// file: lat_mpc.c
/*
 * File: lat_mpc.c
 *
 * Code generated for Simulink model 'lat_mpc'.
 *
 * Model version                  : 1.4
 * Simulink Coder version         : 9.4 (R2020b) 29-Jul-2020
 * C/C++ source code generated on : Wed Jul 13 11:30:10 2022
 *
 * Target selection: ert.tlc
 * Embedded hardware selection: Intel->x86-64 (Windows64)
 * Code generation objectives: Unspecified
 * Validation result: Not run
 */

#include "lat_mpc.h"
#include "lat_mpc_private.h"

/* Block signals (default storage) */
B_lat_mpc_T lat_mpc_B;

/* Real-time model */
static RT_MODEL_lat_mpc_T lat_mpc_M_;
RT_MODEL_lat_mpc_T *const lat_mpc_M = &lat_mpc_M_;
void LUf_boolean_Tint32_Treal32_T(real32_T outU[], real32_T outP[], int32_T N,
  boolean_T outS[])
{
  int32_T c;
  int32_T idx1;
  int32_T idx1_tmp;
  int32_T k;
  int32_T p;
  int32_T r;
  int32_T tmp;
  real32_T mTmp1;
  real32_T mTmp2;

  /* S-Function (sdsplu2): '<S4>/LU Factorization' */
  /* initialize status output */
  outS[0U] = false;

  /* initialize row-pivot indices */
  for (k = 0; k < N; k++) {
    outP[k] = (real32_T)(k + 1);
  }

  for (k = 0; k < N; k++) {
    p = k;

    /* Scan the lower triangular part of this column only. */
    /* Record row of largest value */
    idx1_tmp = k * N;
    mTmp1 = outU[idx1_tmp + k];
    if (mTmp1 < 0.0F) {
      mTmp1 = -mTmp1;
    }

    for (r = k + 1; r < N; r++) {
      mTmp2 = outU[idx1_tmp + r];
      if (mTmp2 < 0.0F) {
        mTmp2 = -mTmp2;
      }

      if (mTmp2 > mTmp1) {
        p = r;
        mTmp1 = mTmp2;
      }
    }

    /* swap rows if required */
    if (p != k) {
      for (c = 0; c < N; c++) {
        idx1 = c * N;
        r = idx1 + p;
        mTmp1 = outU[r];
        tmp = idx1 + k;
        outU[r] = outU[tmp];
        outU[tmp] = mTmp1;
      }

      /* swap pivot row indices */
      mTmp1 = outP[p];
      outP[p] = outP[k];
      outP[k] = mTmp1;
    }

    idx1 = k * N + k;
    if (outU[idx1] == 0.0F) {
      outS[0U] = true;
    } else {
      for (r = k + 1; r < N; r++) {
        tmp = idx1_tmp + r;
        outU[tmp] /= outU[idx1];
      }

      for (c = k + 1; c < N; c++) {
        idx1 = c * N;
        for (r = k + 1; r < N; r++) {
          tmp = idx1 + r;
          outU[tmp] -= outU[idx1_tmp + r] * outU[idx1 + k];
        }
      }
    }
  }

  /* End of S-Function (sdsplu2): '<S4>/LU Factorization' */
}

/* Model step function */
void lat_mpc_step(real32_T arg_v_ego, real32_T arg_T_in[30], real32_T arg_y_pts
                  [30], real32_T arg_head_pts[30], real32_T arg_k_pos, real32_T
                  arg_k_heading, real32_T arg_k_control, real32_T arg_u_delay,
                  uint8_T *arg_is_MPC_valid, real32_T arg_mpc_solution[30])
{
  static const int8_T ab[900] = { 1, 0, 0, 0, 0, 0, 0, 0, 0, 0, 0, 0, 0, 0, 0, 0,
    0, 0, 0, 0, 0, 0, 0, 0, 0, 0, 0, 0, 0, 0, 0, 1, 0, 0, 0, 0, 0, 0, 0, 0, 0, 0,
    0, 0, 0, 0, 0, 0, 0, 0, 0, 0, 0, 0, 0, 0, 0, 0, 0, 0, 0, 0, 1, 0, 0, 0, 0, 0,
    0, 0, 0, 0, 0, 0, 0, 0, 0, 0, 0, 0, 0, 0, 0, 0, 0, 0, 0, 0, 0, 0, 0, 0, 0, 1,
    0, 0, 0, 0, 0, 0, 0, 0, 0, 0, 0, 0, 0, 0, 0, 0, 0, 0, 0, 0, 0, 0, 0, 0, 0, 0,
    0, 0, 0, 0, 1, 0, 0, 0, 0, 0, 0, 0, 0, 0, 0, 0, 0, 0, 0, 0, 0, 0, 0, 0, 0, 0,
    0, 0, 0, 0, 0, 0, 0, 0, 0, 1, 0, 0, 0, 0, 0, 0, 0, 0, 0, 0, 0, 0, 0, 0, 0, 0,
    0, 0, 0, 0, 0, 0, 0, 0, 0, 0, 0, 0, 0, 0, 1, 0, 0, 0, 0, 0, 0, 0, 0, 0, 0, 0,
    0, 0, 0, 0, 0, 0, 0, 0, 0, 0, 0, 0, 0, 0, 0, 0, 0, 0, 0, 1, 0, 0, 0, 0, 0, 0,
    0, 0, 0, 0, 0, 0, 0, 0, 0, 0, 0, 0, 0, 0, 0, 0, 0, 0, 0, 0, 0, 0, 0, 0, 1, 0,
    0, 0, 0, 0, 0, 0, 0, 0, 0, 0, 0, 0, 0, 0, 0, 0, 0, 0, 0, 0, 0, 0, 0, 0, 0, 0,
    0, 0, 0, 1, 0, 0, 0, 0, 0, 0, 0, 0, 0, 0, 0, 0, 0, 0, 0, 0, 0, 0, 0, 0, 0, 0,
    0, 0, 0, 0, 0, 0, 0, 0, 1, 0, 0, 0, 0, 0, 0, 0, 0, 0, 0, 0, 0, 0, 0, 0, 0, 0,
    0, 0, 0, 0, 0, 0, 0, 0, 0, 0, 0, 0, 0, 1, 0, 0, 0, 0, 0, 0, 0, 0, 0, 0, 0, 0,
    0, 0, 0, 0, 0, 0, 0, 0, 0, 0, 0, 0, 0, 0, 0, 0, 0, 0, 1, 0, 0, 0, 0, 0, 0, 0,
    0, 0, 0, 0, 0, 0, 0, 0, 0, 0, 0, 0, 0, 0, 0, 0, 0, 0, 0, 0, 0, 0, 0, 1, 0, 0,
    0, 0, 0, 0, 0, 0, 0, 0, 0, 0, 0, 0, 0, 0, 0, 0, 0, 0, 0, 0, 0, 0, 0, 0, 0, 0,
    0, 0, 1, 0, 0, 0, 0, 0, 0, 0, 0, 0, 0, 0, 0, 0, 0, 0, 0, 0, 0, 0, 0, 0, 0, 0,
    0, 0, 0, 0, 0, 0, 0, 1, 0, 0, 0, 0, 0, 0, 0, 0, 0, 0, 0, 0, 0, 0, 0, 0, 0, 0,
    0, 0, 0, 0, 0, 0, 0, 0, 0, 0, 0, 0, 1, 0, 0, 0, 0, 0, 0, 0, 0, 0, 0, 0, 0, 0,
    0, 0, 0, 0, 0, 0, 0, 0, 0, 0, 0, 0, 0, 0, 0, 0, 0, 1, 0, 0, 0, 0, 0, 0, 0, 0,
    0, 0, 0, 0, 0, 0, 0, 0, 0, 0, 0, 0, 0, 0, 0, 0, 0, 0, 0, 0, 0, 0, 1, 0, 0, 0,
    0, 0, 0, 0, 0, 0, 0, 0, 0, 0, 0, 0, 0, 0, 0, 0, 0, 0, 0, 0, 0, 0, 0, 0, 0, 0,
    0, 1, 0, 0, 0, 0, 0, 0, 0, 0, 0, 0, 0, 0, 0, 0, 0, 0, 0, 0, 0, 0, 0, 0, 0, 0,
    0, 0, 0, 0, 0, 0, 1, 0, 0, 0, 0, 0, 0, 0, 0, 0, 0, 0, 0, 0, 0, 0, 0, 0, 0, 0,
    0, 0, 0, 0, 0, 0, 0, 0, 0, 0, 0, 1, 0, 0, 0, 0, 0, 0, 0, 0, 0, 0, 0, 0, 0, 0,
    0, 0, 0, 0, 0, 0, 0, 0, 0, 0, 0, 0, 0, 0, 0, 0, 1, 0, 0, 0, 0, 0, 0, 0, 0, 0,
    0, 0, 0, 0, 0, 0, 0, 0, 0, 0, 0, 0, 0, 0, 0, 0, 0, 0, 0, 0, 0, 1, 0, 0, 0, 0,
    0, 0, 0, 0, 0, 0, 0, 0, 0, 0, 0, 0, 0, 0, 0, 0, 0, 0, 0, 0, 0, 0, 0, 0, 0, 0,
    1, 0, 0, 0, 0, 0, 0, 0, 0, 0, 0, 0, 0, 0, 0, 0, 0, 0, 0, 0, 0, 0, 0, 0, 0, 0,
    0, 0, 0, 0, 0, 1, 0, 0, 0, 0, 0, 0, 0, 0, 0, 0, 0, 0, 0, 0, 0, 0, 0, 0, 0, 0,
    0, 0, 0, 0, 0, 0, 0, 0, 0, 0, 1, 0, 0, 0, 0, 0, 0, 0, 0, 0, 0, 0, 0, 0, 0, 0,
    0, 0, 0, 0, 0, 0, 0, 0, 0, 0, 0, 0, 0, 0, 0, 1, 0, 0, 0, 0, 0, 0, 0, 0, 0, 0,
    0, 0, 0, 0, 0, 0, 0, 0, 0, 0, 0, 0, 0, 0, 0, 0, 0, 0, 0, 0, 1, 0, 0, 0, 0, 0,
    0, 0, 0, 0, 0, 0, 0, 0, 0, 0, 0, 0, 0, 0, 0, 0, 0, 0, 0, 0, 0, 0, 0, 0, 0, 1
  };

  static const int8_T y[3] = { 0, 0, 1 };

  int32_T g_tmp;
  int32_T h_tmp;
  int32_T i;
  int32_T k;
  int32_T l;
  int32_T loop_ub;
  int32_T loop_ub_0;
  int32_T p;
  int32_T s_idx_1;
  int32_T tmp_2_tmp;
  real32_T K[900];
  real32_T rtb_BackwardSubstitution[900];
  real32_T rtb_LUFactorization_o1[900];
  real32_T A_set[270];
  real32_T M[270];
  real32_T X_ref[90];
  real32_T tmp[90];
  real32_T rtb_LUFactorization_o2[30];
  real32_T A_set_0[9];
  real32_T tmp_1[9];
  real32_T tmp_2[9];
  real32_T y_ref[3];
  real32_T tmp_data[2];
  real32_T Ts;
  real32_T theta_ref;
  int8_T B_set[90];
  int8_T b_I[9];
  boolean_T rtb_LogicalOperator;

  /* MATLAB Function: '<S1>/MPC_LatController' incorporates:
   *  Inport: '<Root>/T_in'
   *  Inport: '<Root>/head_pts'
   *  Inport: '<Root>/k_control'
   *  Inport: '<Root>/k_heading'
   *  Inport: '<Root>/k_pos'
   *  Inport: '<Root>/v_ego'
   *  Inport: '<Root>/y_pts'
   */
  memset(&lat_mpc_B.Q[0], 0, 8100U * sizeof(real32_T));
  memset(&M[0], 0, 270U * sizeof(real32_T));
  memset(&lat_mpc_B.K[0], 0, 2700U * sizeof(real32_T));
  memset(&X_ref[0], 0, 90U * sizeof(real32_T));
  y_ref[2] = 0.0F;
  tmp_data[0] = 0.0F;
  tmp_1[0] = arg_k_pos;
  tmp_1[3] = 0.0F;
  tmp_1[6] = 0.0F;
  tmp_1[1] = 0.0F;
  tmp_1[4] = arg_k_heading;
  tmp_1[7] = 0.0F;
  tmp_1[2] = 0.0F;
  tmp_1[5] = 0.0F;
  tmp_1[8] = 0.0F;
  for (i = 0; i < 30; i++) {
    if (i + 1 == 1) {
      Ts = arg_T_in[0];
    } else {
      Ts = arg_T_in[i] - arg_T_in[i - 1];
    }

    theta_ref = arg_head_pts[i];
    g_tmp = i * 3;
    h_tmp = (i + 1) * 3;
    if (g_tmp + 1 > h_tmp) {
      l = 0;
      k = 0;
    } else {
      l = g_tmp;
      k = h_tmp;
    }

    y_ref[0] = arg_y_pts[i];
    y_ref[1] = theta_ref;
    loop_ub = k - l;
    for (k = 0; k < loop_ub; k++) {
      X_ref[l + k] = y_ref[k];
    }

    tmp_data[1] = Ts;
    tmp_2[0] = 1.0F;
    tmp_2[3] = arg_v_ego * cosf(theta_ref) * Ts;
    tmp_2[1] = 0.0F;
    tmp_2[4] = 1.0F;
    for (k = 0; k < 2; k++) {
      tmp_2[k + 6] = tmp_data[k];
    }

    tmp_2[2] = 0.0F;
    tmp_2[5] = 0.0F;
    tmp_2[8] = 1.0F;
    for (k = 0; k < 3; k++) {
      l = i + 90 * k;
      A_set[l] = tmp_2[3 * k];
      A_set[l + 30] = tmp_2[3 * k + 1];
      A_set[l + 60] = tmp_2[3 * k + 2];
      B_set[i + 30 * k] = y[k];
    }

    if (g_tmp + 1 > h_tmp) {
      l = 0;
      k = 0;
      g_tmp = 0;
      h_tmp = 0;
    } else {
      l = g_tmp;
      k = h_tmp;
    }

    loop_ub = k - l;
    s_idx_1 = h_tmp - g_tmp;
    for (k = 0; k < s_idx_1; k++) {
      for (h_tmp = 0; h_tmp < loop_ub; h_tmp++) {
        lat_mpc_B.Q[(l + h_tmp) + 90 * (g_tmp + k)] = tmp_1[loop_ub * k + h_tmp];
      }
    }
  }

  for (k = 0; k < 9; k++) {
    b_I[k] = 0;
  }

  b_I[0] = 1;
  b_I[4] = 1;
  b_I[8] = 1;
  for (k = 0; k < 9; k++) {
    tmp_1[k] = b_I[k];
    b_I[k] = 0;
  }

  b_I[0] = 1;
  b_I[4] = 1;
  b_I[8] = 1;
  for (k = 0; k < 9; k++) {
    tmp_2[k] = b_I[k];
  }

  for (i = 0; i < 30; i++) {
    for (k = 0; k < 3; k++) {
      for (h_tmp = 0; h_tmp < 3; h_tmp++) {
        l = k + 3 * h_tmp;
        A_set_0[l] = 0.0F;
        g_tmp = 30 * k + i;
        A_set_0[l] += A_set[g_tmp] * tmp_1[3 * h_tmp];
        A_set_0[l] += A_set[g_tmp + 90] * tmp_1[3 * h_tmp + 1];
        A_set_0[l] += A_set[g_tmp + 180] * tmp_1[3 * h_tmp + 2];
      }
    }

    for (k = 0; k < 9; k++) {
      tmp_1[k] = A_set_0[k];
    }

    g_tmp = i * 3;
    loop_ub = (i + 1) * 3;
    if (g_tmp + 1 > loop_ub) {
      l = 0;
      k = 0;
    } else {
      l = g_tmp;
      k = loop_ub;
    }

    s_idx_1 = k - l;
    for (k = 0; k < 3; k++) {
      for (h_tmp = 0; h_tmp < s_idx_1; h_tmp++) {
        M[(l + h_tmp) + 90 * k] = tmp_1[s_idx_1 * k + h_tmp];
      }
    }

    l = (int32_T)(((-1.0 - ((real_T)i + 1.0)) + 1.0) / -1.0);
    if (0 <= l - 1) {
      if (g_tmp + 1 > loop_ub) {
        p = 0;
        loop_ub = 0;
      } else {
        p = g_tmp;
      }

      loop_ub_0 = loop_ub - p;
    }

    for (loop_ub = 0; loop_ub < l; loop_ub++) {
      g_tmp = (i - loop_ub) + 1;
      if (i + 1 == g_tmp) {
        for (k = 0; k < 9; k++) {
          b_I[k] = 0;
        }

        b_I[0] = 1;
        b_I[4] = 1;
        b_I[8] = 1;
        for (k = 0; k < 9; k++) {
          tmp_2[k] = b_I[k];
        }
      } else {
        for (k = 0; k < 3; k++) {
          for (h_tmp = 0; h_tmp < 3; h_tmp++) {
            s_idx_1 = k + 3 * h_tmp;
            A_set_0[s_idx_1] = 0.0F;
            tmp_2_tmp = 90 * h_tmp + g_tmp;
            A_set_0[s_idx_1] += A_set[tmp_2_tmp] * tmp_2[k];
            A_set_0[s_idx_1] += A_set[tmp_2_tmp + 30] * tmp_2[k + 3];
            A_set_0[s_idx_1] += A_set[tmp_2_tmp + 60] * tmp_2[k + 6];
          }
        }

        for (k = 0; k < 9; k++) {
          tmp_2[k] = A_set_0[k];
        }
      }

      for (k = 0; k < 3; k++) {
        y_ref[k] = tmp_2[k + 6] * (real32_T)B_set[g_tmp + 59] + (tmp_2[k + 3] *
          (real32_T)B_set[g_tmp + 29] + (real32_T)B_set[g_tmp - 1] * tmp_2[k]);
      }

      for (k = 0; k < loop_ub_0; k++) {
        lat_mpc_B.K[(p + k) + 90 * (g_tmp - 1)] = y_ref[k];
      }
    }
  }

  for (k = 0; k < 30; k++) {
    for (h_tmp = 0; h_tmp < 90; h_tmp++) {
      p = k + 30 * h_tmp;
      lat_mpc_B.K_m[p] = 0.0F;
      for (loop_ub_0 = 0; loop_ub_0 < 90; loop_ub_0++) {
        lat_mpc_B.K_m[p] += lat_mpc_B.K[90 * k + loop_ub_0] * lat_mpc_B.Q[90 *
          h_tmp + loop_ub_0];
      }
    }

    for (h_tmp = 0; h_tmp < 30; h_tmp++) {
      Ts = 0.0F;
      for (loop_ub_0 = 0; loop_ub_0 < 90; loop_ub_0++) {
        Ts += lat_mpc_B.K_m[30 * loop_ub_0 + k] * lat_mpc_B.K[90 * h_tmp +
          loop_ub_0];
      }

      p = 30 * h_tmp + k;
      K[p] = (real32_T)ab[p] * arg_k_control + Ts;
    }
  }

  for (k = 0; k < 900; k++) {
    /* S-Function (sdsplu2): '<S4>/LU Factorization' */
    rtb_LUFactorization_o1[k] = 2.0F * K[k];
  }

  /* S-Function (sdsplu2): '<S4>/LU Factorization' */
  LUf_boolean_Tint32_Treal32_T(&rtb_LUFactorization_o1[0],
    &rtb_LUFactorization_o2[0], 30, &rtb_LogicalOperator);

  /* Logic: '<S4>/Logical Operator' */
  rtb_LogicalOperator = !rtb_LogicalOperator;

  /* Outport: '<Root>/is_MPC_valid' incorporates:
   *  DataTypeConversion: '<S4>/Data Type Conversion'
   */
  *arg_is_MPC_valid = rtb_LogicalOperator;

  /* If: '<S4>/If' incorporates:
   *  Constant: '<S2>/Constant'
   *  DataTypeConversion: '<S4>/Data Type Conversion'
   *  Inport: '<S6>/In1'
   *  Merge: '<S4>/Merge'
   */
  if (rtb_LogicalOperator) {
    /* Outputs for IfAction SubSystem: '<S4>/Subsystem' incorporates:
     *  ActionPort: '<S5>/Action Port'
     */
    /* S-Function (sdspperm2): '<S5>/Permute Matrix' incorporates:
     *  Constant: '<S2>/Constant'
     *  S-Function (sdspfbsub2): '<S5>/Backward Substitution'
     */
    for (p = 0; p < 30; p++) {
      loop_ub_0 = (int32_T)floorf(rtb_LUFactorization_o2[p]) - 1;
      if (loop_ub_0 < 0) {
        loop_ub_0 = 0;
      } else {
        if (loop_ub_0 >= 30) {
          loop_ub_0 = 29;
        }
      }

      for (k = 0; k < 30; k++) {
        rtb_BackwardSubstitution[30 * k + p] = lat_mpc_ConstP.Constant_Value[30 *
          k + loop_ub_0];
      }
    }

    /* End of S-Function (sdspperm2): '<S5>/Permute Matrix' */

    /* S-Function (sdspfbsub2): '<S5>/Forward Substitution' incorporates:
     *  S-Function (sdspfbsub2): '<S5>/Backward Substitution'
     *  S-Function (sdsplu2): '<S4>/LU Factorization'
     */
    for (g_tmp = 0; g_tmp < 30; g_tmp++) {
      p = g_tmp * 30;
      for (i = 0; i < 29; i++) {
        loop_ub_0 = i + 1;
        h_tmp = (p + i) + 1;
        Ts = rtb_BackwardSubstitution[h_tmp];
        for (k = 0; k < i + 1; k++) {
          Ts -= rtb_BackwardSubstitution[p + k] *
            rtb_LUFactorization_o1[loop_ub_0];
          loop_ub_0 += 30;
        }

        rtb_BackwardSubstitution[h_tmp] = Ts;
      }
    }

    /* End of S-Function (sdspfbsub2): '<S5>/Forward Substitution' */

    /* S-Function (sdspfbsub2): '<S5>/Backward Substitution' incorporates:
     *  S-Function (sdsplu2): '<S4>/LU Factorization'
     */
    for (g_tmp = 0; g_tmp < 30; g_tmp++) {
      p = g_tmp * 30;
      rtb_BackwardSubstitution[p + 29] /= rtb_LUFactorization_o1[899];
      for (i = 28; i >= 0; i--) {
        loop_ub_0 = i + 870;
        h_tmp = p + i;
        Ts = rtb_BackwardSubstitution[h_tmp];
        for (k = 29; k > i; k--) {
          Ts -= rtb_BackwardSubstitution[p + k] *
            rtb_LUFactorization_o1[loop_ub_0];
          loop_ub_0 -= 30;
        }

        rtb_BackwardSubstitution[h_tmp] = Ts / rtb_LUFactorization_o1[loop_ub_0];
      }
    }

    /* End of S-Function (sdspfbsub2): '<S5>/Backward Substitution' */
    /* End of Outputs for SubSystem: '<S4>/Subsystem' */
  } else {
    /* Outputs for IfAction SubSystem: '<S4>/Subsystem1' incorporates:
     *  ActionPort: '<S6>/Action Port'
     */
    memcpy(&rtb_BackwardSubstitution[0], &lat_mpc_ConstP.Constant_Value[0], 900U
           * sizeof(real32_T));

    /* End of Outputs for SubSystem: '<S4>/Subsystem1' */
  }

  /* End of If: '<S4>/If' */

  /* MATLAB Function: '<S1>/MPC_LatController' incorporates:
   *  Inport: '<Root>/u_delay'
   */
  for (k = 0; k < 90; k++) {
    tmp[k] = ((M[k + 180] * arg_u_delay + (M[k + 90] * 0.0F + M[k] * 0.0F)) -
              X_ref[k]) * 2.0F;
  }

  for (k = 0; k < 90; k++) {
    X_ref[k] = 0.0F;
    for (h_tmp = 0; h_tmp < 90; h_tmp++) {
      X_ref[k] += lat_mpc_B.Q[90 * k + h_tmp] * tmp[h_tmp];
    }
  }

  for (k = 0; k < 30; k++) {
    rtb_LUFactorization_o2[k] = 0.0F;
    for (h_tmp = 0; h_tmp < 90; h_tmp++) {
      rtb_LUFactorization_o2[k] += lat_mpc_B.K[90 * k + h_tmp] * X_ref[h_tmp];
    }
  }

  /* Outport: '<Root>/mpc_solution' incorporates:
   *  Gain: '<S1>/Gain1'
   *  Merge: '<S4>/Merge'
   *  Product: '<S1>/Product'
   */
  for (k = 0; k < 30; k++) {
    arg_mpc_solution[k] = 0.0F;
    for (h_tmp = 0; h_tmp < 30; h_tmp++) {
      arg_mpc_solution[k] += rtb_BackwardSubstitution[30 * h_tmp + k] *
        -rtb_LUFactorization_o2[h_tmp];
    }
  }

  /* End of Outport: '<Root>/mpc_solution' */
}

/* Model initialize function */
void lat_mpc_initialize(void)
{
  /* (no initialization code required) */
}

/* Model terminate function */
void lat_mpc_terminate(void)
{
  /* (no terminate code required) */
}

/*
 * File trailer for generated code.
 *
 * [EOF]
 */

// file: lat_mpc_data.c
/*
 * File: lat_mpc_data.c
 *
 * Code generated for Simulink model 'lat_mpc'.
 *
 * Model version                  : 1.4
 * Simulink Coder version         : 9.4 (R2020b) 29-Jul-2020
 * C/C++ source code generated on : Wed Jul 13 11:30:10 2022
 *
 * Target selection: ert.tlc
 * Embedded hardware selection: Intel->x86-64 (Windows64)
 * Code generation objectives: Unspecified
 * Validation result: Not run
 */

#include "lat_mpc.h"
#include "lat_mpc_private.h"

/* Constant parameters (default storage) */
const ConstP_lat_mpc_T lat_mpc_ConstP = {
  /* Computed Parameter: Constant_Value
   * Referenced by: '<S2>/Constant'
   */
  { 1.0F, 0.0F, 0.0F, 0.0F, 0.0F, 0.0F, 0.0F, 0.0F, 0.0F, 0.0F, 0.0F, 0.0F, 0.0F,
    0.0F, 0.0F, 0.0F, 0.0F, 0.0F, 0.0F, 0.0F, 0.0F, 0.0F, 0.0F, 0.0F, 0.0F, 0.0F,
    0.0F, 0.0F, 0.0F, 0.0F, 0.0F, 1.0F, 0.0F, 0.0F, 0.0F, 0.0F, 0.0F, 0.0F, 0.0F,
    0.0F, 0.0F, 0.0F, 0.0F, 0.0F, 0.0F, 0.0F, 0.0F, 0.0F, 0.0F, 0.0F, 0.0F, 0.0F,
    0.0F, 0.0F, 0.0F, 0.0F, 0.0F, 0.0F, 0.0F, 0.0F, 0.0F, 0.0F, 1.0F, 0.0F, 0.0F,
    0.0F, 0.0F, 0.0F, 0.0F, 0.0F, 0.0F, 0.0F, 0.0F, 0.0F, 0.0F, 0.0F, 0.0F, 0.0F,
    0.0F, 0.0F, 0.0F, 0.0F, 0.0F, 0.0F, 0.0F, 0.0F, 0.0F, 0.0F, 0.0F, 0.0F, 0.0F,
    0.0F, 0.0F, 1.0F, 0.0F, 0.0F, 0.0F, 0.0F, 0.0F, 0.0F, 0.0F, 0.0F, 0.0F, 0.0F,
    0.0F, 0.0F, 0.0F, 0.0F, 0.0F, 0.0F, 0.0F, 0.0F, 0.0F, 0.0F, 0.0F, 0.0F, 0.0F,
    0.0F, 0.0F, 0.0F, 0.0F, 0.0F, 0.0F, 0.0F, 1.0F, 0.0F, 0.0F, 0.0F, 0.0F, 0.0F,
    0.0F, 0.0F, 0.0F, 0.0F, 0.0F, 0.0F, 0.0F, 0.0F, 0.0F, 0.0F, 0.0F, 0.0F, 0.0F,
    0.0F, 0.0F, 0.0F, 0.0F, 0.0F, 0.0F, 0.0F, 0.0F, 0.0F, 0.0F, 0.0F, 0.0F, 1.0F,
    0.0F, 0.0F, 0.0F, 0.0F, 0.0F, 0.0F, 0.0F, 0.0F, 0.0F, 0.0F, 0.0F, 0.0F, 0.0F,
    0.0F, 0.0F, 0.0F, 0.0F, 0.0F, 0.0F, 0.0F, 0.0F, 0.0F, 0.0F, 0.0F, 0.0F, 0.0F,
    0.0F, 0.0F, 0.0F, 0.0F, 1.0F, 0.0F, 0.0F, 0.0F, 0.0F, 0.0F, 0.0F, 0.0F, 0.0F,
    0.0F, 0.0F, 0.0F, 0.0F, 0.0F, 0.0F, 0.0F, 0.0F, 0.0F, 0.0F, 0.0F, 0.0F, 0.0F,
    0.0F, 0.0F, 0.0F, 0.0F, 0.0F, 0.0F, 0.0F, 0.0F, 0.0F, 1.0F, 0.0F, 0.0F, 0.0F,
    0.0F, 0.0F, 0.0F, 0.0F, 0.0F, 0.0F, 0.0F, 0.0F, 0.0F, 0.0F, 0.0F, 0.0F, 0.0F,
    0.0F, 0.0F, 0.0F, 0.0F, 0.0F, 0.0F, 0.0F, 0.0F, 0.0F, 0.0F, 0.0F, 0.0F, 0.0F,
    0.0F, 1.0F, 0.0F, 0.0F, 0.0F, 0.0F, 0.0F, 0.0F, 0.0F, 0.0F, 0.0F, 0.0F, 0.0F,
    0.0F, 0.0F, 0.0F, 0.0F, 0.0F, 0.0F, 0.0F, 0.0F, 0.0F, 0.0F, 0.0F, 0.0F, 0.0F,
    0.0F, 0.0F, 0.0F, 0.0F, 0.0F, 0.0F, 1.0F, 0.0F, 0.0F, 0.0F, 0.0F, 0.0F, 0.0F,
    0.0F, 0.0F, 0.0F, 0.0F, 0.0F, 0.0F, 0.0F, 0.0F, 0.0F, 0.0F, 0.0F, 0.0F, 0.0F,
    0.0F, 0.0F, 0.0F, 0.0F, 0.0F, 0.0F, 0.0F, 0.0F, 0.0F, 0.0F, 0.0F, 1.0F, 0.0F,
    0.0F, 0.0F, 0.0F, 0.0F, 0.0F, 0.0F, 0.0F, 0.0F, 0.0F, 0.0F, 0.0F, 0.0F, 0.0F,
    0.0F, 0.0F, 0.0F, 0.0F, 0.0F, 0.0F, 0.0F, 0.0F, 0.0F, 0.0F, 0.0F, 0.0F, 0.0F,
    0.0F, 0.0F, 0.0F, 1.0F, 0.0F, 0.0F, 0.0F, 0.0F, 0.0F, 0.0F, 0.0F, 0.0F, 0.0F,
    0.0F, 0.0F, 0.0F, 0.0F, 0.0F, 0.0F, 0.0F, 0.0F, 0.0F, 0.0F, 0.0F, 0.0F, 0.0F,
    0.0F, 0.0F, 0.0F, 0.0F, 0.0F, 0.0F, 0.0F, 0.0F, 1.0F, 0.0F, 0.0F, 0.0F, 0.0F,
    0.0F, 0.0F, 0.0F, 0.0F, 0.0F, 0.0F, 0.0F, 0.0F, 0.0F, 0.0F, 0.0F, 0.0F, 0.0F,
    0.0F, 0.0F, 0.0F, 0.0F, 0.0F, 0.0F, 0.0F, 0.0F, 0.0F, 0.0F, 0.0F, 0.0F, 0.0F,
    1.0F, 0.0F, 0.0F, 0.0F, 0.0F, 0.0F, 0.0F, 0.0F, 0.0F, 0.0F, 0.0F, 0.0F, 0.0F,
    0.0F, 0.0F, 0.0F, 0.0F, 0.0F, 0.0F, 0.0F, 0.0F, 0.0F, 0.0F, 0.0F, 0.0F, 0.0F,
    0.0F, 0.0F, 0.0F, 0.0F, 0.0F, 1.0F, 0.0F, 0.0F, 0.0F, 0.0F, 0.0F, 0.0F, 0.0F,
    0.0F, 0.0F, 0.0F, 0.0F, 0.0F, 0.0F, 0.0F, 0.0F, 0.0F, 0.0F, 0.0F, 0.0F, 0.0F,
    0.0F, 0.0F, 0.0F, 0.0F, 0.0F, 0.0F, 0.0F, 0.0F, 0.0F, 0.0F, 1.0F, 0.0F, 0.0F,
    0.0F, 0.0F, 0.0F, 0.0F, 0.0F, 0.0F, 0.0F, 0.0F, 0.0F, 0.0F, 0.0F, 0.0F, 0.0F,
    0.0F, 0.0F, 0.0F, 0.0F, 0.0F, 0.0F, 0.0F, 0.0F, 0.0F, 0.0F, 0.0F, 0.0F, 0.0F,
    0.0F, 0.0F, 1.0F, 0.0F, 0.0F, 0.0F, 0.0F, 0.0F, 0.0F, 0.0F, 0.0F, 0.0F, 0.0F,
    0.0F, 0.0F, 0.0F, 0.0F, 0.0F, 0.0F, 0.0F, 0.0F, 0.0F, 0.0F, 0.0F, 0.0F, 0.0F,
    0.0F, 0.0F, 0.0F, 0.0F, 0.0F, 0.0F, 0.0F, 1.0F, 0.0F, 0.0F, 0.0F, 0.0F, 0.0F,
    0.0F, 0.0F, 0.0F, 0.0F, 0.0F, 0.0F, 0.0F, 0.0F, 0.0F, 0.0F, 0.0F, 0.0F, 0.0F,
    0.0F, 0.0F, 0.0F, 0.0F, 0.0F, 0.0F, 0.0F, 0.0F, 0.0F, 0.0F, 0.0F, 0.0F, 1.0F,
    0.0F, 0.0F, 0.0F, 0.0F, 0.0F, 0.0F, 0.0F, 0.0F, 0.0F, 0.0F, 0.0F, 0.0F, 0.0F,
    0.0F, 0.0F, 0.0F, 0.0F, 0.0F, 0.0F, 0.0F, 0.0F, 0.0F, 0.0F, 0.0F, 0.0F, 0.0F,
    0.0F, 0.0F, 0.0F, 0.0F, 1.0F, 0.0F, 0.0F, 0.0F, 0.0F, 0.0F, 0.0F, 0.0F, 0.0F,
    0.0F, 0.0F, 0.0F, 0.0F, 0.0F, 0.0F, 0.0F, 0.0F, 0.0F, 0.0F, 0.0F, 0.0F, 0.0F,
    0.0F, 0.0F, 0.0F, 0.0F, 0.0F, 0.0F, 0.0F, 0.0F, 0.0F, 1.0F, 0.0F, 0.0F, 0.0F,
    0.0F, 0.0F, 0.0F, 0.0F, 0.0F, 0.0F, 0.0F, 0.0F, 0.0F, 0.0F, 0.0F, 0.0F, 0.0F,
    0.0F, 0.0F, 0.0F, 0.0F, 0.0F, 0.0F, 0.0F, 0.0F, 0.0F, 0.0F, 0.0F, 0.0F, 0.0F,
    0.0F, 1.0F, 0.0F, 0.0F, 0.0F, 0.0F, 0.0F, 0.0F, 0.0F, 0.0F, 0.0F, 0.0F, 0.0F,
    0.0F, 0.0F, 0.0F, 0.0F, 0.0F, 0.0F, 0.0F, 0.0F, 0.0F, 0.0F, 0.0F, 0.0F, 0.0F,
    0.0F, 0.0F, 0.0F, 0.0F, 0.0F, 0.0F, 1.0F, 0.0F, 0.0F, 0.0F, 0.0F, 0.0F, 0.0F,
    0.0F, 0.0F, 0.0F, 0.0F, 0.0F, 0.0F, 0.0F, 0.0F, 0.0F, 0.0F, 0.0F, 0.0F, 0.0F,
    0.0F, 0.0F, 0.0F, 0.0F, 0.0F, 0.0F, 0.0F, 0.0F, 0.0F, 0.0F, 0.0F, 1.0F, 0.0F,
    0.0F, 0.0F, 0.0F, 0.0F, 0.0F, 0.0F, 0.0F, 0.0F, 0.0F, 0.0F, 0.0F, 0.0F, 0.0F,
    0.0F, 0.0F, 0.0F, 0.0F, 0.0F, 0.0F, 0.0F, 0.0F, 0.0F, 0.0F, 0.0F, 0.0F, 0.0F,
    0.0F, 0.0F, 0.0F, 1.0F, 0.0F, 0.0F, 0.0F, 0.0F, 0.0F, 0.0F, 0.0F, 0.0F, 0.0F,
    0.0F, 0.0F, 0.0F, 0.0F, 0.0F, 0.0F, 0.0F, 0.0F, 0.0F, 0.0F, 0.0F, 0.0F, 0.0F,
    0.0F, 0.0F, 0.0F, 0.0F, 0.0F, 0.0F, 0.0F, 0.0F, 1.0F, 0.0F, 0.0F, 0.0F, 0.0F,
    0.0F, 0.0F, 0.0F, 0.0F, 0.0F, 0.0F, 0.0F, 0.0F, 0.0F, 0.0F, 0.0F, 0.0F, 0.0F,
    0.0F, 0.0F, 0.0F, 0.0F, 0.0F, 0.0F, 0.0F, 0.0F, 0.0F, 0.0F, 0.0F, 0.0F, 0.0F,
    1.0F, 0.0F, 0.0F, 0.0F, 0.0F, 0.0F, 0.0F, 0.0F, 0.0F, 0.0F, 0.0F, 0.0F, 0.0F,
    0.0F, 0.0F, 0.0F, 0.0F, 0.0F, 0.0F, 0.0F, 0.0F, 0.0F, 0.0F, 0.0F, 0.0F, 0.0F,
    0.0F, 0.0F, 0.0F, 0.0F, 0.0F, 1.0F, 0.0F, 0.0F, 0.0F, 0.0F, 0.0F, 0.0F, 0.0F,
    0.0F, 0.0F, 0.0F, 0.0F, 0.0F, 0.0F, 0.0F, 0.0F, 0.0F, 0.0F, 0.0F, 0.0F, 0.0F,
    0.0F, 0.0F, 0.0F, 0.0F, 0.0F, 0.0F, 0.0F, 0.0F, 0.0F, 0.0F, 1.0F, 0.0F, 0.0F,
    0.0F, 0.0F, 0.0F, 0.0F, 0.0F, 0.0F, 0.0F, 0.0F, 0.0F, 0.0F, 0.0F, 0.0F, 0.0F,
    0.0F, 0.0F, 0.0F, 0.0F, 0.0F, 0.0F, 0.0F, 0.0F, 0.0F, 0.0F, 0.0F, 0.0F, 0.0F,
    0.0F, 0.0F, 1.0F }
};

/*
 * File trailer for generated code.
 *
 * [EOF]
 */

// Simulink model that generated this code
simulink model "lat_mpc"  (R2020b)
settings: Solver=FixedStepDiscrete  StartTime=0.0  StopTime=10.0  FixedStep=0.05  RelTol=1e-3
undefined symbols (not defined in the file): D
libraries: dspsolvers x2, dspfactors x1, dspsigattribs x1, dspmtrx3 x1

== system lat_mpc ==
  v_ego : Inport  OutDataTypeStr=single
  T_in : Inport  Port=2  OutDataTypeStr=single  PortDimensions=[1 30]
  y_pts : Inport  Port=3  OutDataTypeStr=single
  head_pts : Inport  Port=4  OutDataTypeStr=single
  k_pos : Inport  Port=5  OutDataTypeStr=single
  k_heading : Inport  Port=6  OutDataTypeStr=single
  k_control : Inport  Port=7  OutDataTypeStr=single
  u_delay : Inport  Port=8  OutDataTypeStr=single
  Subsystem : Subsystem
  is_MPC_valid : Outport  VectorParamsAs1DForOutWhenUnconnected=off
  mpc_solution : Outport  Port=2
  wires:
  Subsystem/1(is_MPC_valid) -> is_MPC_valid/1
  Subsystem/2(mpc_solution) -> mpc_solution/1
  v_ego/1 -> Subsystem/1(v)
  T_in/1 -> Subsystem/2(T_in)
  y_pts/1 -> Subsystem/3(y_pts)
  head_pts/1 -> Subsystem/4(head_pts)
  k_pos/1 -> Subsystem/5(k_pos)
  k_heading/1 -> Subsystem/6(k_heading)
  k_control/1 -> Subsystem/7(k_control)
  u_delay/1 -> Subsystem/8(u_delay)

== system lat_mpc/Subsystem ==
  v : Inport
  T_in : Inport  Port=2
  y_pts : Inport  Port=3
  head_pts : Inport  Port=4
  k_pos : Inport  Port=5
  k_heading : Inport  Port=6
  k_control : Inport  Port=7
  u_delay : Inport  Port=8
  Gain1 : Gain  Gain=-1
  Hissien_Matrix_Inverse : Subsystem  AncestorBlock=dspinverses/ LU Inverse  mask(LU Inverse){}
      mask help: Matrix inverse using LU factorization.
  MPC_LatController : MATLAB Function  TreatAsAtomicUnit=on
  Product : Product  Inputs=**  Multiplication=Matrix(*)
  Reshape : Reshape  OutputDimensionality=Column vector (2-D)
  is_MPC_valid : Outport  VectorParamsAs1DForOutWhenUnconnected=off
  mpc_solution : Outport  Port=2
  wires:
  Hissien_Matrix_Inverse/1(X_inv) -> Product/1
  Hissien_Matrix_Inverse/2(is_MPC_valid) -> is_MPC_valid/1
  MPC_LatController/1(H) -> Hissien_Matrix_Inverse/1(A)
  Gain1/1 -> Product/2
  Reshape/1 -> Gain1/1
  y_pts/1 -> MPC_LatController/3(y_pts)
  head_pts/1 -> MPC_LatController/4(head_pts)
  Product/1 -> mpc_solution/1
  u_delay/1 -> MPC_LatController/8(u_delay)
  v/1 -> MPC_LatController/1(v)
  MPC_LatController/2(f) -> Reshape/1
  k_heading/1 -> MPC_LatController/6(k_heading)
  k_control/1 -> MPC_LatController/7(k_control)
  k_pos/1 -> MPC_LatController/5(k_pos)
  T_in/1 -> MPC_LatController/2(T_in)

== system lat_mpc/Subsystem/Hissien_Matrix_Inverse ==
  A : Inport  OutDataTypeStr=single  PortDimensions=[30 30]
  Constant : Constant  Value=eye(30, 30)  OutDataTypeStr=single
  LU Solver : Subsystem  AncestorBlock=dspsolvers/LU Solver  mask(LU Solver){}
      mask help: dsp:dspsolvers:LUSolver_MD
      mask init:
      | x=[ 0.135 .475 0.475 0.135 .135 NaN 0.55 0.64 0.64 0.55 0.55 NaN 0.685 0.73 NaN 0.685 0.73 NaN 0.775 0.865 0.865 0.775 0.775 ];
      | y=[ 0.2 0.2 0.7 0.7 0.2 NaN 0.2 0.2 0.7 0.7 0.2 NaN 0.4 0.4 NaN 0.45 0.45 NaN 0.2 0.2 0.7 0.7 0.2 ];
  X_inv : Outport  VectorParamsAs1DForOutWhenUnconnected=off
  is_MPC_valid : Outport  Port=2  VectorParamsAs1DForOutWhenUnconnected=off
  wires:
  A/1 -> LU Solver/1(A)
  LU Solver/1(X) -> X_inv/1
  LU Solver/2(is_MPC_valid) -> is_MPC_valid/1
  Constant/1 -> LU Solver/2(B)

== system lat_mpc/Subsystem/Hissien_Matrix_Inverse/LU Solver ==
  A : Inport
  B : Inport  Port=2
  Data Type Conversion : DataTypeConversion  OutDataTypeStr=uint8
  If : If  IfExpression=u1 ~= 0
  LU Factorization : dspfactors/LU Factorization  singular=on  roundingMode=Floor  overflowMode=off  outputMin=[]  outputMax=[]
  Logical Operator : Logic  Operator=NOT  AllPortsSameDT=off  OutDataTypeStr=boolean
  Merge : Merge
  Subsystem : Subsystem
  Subsystem1 : Subsystem
  X : Outport  InitialOutput=0  VectorParamsAs1DForOutWhenUnconnected=off
  is_MPC_valid : Outport  Port=2  VectorParamsAs1DForOutWhenUnconnected=off
  wires:
  A/1 -> LU Factorization/1
  LU Factorization/1 -> Subsystem/1(L)
  LU Factorization/2 -> Subsystem/2(P)
  B/1 -> Subsystem1/1(In1), Subsystem/3(B)
  LU Factorization/3 -> Logical Operator/1
  Logical Operator/1 -> Data Type Conversion/1
  Data Type Conversion/1 -> is_MPC_valid/1, If/1
  If/1 -> Subsystem/Action
  If/2 -> Subsystem1/Action
  Subsystem1/1(Out1) -> Merge/2
  Subsystem/1(Out1) -> Merge/1
  Merge/1 -> X/1

== system lat_mpc/Subsystem/Hissien_Matrix_Inverse/LU Solver/Subsystem ==
  L : Inport
  P : Inport  Port=2
  B : Inport  Port=3
  Action Port : ActionPort  ActionPortLabel=if(u1 ~= 0)
  Backward Substitution : dspsolvers/Backward Substitution  Unit=off  RealDiag=off  roundingMode=Floor  overflowMode=off  accumDataTypeStr=Inherit: Same as product output  accumLastDataTypeStr=Inherit: Same as product output  outputMin=[]  outputMax=[]
  Check Signal Attributes2 : dspsigattribs/Check Signal Attributes  SigAttribCheckMethod=Does not match attributes exactly  Complexity=Ignore  Frame=Ignore  DimsCheckMethod=Ignore  Dimensions=1-D  DatatypeCheckMethod=Is...  DatatypeGeneral=Floating-point  DtypeFloatSpecific=Any floating-point  DtypeFixedSpecific=Any fixed-point  DtypeIntSpecific=Any integer  SampleMode=Ignore
  Forward Substitution : dspsolvers/Forward Substitution  Unit=on  RealDiag=on  roundingMode=Floor  overflowMode=off  accumDataTypeStr=Inherit: Same as product output  accumLastDataTypeStr=Inherit: Same as product output  outputMin=[]  outputMax=[]
  Permute Matrix : dspmtrx3/Permute Matrix  mode=Rows  ZeroOneIdxMode=One-based  errmode=Clip index  checkDims=on
  Out1 : Outport  VectorParamsAs1DForOutWhenUnconnected=off
  wires:
  Backward Substitution/1 -> Check Signal Attributes2/1
  B/1 -> Permute Matrix/1
  P/1 -> Permute Matrix/2
  Check Signal Attributes2/1 -> Out1/1
  Forward Substitution/1 -> Backward Substitution/2  "y"
  L/1 -> Forward Substitution/1, Backward Substitution/1
  Permute Matrix/1 -> Forward Substitution/2

== system lat_mpc/Subsystem/Hissien_Matrix_Inverse/LU Solver/Subsystem1 ==
  In1 : Inport
  Action Port : ActionPort  ActionPortLabel=else
  Out1 : Outport  VectorParamsAs1DForOutWhenUnconnected=off
  wires:
  In1/1 -> Out1/1

== matlab function lat_mpc/Subsystem/MPC_LatController ==
function [H, f] = fcn(v, T_in, y_pts, head_pts, k_pos, k_heading, k_control, u_delay)

%% define controller parameters
p = 30;  % mpc predicted steps 
state_len = 3; % number of states

%% matrix initialization
% Q, R weight matrix 
Q = single(zeros(state_len*p, state_len*p)); 
R = single(k_control*eye(p)); 

% state transition matrix
A = single(zeros(3,3));
B = single(zeros(3,1));
A_ = single(zeros(3,3));
B_ = single(zeros(3,1));
A_set = single(zeros(p, 3, 3));
B_set = single(zeros(p, 3, 1));

% middle layer matrix
M = single(zeros(state_len*p, state_len));
K = single(zeros(state_len*p, p));

% reference desired state 
X_ref = single(zeros(state_len*p, 1));
yawrate_ref = single(zeros(p,1));
theta_ref = single(zeros(p,1));
y_ref = single(zeros(p, 1));

% QP solver matrix
H = single(zeros(p, p));
f = single(zeros(p, 1));

%% time array caculation
T =  T_in;

% referce x array
x_ref = v.*T;

%% intial states
x = single([0; 0; u_delay]); 

%% caculate X_ref, give the value for Q,R
% control input is delta of omiga
% matrix X_
%           |  y      | 
% X_ =	    |  theta  | 
%           |  omiga  | 

% matrix A_
%           |1    v*cos(theta)   0 | 
% A_ =	    |0    1             Ts | 
%           |0    0              1 | 

% matrix B_
%           |  0  | 
% B_ =	    |  0  | 
%           |  1  | 

% if X(k+1) = A*X(k) + B*u
% |X(k+1)|  | A   B | |X(k)|   |0|
%         =          *       + |0| * delta(u)
% |u(k+1)|  | 0   1 | |u(k)|   |1|

for i=1:p
    if i==1
        Ts = T(1);
    else
        Ts = T(i) - T(i-1);
    end

    % reference state
    x_tmp = x_ref(i);
    y_ref(i) = y_pts(i);
    theta_ref(i) = head_pts(i) ;
    yawrate_ref(i) = 0;
    X_ref((i-1)*state_len + 1:state_len*i, 1) = [y_ref(i) theta_ref(i) yawrate_ref(i) ];    
    
    % update A_, B_ set
    A_ = single([1 v*cos(theta_ref(i))*Ts; 0 1]);
    B_ = single([0 ; Ts]);

    A_set(i,:,:) = single([A_ B_; 0 0 1]);
    B_set(i,:,:) = single([0; 0 ;1]);
    
    % update Q weight matrix
    Q((i-1)*state_len + 1:state_len*i,  (i-1)*state_len + 1:state_len*i) = single([k_pos 0 0; 0 k_heading 0; 0 0 0]);

end

%% caculate M, K matrix
tmp_1 = single(eye(3));
tmp_2 = single(eye(3));

% M matrix update
% |  A1
% |  A2A1
% |  A3A2A1
% ..........

% K matrix update
% |0 0 0 ... 0            0         B1|
% |0 0 0 ... 0            A2B1  B2|
% |0 0 0 ... A3A2B1 A3B2  B3|
for i=1:p
   tmp_1 = reshape(A_set(i,:,:), [3 3])*tmp_1;
   M((i-1)*state_len + 1:state_len*i, 1:state_len) = tmp_1;

      for j=i:-1:1
        if j==i
            tmp_2 = single(eye(3));
        else
            tmp_2 = tmp_2*reshape(A_set(j+1,:,:), [3 3]);
        end
       K((i-1)*state_len + 1:state_len*i, j) = tmp_2*reshape(B_set(j,:,:), [3 1]);

      end
   
      
end

%% caculate H, f matrix for QP solver
X_pre = M*x;
E = X_pre - X_ref;

H = 2*(K'*Q*K + R);
f = (2*E'*Q*K)';

end

function prv_yawrate = preview_yawrate_calc(C1, C2, C3,C4, C5, d, v)
    ddy = 2*C2 + 6*C3*d + 12*C4*d^2 + 20*C5*d^3;
    
    dy = C1 + 2*C2*d + 3*C3*d^2+ 4*C4*d^3 +5*C5*d^4  ;
    
    prv_curve = ddy/((1+dy^2)^1.5);
    
    prv_yawrate = prv_curve * v;

end
